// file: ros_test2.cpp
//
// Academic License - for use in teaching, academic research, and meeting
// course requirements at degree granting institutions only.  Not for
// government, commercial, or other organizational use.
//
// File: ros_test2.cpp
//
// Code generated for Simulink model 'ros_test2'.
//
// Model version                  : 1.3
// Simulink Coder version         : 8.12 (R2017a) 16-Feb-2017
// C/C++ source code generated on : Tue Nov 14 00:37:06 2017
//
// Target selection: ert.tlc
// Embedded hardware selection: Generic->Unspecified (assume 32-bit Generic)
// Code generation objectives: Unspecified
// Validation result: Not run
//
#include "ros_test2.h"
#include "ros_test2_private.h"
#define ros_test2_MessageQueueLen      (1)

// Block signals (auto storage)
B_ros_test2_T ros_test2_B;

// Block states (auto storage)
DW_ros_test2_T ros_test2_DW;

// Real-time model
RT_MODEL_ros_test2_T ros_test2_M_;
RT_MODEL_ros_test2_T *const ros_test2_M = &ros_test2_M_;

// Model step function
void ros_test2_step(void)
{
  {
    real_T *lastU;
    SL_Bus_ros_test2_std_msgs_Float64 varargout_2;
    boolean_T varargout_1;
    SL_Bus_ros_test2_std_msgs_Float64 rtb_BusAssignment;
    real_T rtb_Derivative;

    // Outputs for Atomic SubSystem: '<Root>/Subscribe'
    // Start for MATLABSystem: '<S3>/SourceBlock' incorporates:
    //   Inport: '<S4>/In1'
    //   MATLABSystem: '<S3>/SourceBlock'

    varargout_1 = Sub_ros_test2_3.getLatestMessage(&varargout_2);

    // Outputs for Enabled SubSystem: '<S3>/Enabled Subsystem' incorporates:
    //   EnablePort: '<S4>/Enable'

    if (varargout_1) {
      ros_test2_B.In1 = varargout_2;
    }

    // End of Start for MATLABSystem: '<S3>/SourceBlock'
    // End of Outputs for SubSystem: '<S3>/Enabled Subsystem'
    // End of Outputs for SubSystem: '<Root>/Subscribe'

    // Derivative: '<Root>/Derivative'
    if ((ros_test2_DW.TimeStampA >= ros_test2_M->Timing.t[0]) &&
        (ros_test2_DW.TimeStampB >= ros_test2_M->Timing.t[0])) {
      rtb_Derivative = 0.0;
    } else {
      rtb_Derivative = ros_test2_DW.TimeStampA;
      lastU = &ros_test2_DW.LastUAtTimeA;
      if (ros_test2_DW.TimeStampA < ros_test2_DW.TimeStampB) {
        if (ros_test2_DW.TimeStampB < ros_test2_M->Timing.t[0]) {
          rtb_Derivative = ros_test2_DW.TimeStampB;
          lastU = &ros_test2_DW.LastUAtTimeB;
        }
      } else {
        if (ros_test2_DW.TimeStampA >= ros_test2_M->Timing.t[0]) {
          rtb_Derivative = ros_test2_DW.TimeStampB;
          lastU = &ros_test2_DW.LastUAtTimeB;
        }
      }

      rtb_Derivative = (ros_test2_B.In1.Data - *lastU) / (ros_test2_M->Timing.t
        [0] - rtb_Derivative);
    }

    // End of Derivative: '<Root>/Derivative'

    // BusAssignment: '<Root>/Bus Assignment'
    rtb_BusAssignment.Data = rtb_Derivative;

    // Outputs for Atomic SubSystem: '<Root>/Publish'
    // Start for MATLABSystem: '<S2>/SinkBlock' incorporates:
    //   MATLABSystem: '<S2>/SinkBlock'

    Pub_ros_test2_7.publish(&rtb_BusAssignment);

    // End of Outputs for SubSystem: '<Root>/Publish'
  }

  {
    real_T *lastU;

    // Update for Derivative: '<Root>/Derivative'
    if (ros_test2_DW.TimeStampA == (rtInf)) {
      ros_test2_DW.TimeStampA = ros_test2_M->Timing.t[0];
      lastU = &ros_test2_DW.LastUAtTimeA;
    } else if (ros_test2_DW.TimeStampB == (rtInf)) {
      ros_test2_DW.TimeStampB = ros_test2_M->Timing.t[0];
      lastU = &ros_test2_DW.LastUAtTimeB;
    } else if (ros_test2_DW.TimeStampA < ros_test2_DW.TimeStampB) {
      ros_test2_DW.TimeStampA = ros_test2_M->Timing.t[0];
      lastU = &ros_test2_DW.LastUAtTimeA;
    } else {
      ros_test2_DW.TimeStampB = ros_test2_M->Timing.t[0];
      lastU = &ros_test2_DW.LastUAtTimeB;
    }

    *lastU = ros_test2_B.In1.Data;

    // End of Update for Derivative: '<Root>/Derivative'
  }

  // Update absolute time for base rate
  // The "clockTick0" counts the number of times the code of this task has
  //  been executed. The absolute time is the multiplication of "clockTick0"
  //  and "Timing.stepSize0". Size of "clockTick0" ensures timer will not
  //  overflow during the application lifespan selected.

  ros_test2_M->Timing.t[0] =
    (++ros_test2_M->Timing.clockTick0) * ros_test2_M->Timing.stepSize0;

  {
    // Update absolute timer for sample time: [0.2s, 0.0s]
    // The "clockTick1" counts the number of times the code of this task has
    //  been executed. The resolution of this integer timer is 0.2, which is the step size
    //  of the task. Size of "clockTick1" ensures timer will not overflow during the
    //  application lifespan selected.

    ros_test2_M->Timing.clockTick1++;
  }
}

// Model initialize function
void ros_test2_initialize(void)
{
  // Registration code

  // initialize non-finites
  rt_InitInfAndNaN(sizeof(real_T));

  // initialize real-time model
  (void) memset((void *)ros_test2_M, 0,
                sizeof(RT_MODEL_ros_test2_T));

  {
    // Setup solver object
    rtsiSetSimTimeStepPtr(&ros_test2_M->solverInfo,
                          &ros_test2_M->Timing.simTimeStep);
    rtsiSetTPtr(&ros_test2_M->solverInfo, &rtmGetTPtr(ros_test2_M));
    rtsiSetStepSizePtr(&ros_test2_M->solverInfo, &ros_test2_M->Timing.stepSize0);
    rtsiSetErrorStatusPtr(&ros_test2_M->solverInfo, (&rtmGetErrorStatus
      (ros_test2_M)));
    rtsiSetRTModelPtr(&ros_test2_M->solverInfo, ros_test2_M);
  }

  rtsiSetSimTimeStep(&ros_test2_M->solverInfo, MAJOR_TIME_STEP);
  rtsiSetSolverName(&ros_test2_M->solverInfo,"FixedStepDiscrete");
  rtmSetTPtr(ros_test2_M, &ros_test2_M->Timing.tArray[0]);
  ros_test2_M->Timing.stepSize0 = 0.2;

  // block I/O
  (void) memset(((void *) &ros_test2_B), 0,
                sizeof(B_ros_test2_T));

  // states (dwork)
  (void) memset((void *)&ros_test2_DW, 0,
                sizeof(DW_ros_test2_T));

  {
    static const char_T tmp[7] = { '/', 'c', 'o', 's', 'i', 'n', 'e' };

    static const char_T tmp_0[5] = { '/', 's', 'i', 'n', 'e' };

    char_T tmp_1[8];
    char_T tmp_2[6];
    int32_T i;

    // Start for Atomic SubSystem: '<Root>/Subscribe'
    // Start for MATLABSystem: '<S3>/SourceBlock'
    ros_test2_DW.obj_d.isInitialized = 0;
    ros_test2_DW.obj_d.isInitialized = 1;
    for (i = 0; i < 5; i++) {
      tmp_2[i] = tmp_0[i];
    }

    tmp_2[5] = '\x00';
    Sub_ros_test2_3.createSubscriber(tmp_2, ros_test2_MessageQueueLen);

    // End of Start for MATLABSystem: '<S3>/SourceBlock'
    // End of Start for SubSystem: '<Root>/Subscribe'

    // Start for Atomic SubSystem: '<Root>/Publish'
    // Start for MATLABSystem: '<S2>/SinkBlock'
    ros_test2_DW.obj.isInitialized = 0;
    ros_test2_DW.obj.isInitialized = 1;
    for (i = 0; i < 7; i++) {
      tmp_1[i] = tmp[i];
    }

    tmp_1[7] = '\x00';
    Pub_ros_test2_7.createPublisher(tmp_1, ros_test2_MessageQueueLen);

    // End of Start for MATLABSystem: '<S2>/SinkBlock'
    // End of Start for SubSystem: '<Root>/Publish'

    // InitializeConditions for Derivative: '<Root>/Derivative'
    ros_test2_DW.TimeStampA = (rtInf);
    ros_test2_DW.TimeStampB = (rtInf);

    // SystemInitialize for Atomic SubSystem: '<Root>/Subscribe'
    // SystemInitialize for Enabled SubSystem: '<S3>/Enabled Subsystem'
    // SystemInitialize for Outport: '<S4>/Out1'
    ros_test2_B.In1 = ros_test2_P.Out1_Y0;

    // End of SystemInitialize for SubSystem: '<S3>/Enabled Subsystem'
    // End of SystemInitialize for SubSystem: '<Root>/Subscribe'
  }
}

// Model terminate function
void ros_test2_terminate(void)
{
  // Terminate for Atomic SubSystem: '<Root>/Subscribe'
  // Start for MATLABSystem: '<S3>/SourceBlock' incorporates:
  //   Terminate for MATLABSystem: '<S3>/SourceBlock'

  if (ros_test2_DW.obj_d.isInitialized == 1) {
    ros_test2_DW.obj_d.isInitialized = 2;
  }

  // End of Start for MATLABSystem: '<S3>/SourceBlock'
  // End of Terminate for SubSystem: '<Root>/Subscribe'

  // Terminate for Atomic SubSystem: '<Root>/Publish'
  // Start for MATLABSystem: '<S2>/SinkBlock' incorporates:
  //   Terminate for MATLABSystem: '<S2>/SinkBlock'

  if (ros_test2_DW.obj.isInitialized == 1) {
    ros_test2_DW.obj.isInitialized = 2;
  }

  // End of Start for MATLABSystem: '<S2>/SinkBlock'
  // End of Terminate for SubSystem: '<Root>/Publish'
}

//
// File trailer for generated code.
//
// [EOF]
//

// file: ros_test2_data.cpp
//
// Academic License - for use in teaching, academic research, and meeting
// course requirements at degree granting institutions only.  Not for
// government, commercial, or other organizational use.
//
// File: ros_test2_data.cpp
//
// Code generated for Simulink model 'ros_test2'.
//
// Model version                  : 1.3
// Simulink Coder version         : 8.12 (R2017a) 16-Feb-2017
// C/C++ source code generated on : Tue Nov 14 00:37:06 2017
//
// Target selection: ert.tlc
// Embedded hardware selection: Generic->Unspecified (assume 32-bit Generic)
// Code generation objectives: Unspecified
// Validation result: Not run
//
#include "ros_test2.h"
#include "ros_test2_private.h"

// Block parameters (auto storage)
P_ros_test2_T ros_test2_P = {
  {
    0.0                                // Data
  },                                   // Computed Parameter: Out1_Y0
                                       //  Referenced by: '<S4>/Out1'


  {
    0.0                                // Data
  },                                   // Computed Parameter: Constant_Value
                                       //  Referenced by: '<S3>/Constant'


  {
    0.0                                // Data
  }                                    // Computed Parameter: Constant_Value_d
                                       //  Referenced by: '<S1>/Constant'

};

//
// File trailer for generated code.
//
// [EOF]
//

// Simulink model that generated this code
simulink model "ros_test2"  (R2017a)
settings: Solver=FixedStepAuto  StartTime=0.0  StopTime=inf  RelTol=1e-3
libraries: robotlib x3

== system ros_test2 ==
  Blank Message : robotlib/Blank Message  SourceLibraryInfo=This block requires Robotics System Toolbox  messageType=std_msgs/Float64  SampleTime=inf
  Bus Assignment : BusAssignment  AssignedSignals=Data
  Bus Selector : BusSelector  OutputSignals=Data
  Derivative : Derivative
  Publish : robotlib/Publish  SourceLibraryInfo=This block requires Robotics System Toolbox  topicSource=Specify your own  topic=/cosine  messageType=std_msgs/Float64  messageQueueLength=1
  Subscribe : robotlib/Subscribe  SourceLibraryInfo=This block requires Robotics System Toolbox  topicSource=Specify your own  topic=/sine  messageType=std_msgs/Float64  sampleTime=-1  messageQueueLength=1
  Terminator : Terminator
  wires:
  Bus Assignment/1 -> Publish/1
  Blank Message/1 -> Bus Assignment/1
  Derivative/1 -> Bus Assignment/2
  Subscribe/1 -> Terminator/1
  Subscribe/2 -> Bus Selector/1
  Bus Selector/1 -> Derivative/1  "<Data>"
